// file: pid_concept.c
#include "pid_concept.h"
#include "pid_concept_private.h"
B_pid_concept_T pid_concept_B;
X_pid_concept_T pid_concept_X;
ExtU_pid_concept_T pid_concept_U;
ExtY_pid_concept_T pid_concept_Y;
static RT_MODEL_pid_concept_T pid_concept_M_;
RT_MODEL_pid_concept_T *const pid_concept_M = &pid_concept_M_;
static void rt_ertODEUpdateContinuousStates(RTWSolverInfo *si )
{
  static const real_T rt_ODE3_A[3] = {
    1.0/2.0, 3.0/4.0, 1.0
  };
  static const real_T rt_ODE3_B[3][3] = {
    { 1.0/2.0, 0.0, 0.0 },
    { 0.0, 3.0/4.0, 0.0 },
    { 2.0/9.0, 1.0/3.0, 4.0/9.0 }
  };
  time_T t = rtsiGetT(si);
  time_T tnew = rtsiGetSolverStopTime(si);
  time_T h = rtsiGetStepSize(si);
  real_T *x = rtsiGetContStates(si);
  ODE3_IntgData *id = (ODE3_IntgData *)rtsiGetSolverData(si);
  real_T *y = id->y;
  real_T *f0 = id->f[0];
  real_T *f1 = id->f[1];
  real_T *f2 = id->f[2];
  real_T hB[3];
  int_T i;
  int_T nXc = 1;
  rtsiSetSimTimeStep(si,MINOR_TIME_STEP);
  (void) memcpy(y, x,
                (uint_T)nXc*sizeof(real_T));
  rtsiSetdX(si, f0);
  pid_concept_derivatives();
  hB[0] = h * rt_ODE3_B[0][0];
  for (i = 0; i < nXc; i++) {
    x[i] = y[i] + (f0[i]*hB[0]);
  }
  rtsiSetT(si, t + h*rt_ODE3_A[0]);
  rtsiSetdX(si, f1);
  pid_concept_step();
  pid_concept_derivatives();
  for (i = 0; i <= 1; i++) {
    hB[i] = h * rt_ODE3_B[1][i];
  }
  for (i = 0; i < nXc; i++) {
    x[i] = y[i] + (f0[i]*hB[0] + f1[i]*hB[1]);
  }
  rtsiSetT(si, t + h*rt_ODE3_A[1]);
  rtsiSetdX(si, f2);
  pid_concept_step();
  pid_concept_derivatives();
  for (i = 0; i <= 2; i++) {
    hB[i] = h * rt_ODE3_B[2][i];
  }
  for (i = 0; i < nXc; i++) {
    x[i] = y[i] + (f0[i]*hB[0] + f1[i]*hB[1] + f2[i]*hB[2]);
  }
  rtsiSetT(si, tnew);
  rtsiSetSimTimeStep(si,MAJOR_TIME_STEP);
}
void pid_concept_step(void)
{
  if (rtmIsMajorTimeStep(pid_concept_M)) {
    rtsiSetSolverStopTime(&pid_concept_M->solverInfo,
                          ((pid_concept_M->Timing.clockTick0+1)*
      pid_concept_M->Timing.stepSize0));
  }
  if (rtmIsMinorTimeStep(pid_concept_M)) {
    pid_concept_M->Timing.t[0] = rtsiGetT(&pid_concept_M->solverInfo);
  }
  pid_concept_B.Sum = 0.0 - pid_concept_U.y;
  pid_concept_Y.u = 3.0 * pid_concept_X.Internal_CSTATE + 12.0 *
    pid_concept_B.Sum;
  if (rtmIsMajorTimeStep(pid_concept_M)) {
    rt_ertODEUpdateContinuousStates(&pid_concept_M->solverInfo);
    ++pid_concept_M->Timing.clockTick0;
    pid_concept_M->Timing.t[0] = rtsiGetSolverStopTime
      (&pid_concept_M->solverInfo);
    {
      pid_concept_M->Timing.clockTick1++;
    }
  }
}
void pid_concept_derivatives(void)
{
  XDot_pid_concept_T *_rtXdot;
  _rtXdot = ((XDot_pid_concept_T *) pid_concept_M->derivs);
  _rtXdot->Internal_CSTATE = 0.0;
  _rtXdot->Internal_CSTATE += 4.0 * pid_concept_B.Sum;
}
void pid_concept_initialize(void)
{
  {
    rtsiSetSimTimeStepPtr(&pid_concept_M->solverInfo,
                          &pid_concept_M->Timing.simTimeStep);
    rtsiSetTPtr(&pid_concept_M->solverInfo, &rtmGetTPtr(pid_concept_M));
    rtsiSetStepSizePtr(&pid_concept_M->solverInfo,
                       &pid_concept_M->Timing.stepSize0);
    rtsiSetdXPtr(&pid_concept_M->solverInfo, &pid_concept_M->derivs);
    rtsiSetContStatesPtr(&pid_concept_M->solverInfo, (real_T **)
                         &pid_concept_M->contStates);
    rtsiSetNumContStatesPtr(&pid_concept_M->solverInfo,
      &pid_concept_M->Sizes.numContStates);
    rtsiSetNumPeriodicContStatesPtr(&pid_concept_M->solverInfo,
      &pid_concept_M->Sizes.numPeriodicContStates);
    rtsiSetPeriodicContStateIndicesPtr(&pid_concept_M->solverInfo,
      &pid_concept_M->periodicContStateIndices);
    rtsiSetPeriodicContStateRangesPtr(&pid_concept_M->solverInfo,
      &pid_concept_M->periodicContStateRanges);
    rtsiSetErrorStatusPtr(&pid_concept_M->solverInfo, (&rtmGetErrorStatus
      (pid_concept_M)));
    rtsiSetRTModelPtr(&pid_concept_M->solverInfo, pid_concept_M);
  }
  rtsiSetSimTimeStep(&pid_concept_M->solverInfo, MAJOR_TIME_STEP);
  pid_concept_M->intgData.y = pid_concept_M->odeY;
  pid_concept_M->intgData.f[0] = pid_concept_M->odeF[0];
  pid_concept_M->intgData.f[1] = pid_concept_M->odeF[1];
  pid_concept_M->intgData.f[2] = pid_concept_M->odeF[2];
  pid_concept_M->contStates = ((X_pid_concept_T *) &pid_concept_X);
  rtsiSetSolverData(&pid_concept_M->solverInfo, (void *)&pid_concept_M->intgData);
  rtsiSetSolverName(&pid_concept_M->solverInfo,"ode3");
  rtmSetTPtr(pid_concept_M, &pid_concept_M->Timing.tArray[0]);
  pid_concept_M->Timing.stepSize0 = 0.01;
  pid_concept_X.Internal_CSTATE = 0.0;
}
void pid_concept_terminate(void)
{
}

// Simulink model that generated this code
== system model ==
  Inport#1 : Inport
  Outport#1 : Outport  <- 1: LTISystem#1
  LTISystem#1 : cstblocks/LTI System  <- 1: Sum
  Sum : Sum  Inputs=+-  <- 1: Constant#1, 2: Inport#1
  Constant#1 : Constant  Value=0
